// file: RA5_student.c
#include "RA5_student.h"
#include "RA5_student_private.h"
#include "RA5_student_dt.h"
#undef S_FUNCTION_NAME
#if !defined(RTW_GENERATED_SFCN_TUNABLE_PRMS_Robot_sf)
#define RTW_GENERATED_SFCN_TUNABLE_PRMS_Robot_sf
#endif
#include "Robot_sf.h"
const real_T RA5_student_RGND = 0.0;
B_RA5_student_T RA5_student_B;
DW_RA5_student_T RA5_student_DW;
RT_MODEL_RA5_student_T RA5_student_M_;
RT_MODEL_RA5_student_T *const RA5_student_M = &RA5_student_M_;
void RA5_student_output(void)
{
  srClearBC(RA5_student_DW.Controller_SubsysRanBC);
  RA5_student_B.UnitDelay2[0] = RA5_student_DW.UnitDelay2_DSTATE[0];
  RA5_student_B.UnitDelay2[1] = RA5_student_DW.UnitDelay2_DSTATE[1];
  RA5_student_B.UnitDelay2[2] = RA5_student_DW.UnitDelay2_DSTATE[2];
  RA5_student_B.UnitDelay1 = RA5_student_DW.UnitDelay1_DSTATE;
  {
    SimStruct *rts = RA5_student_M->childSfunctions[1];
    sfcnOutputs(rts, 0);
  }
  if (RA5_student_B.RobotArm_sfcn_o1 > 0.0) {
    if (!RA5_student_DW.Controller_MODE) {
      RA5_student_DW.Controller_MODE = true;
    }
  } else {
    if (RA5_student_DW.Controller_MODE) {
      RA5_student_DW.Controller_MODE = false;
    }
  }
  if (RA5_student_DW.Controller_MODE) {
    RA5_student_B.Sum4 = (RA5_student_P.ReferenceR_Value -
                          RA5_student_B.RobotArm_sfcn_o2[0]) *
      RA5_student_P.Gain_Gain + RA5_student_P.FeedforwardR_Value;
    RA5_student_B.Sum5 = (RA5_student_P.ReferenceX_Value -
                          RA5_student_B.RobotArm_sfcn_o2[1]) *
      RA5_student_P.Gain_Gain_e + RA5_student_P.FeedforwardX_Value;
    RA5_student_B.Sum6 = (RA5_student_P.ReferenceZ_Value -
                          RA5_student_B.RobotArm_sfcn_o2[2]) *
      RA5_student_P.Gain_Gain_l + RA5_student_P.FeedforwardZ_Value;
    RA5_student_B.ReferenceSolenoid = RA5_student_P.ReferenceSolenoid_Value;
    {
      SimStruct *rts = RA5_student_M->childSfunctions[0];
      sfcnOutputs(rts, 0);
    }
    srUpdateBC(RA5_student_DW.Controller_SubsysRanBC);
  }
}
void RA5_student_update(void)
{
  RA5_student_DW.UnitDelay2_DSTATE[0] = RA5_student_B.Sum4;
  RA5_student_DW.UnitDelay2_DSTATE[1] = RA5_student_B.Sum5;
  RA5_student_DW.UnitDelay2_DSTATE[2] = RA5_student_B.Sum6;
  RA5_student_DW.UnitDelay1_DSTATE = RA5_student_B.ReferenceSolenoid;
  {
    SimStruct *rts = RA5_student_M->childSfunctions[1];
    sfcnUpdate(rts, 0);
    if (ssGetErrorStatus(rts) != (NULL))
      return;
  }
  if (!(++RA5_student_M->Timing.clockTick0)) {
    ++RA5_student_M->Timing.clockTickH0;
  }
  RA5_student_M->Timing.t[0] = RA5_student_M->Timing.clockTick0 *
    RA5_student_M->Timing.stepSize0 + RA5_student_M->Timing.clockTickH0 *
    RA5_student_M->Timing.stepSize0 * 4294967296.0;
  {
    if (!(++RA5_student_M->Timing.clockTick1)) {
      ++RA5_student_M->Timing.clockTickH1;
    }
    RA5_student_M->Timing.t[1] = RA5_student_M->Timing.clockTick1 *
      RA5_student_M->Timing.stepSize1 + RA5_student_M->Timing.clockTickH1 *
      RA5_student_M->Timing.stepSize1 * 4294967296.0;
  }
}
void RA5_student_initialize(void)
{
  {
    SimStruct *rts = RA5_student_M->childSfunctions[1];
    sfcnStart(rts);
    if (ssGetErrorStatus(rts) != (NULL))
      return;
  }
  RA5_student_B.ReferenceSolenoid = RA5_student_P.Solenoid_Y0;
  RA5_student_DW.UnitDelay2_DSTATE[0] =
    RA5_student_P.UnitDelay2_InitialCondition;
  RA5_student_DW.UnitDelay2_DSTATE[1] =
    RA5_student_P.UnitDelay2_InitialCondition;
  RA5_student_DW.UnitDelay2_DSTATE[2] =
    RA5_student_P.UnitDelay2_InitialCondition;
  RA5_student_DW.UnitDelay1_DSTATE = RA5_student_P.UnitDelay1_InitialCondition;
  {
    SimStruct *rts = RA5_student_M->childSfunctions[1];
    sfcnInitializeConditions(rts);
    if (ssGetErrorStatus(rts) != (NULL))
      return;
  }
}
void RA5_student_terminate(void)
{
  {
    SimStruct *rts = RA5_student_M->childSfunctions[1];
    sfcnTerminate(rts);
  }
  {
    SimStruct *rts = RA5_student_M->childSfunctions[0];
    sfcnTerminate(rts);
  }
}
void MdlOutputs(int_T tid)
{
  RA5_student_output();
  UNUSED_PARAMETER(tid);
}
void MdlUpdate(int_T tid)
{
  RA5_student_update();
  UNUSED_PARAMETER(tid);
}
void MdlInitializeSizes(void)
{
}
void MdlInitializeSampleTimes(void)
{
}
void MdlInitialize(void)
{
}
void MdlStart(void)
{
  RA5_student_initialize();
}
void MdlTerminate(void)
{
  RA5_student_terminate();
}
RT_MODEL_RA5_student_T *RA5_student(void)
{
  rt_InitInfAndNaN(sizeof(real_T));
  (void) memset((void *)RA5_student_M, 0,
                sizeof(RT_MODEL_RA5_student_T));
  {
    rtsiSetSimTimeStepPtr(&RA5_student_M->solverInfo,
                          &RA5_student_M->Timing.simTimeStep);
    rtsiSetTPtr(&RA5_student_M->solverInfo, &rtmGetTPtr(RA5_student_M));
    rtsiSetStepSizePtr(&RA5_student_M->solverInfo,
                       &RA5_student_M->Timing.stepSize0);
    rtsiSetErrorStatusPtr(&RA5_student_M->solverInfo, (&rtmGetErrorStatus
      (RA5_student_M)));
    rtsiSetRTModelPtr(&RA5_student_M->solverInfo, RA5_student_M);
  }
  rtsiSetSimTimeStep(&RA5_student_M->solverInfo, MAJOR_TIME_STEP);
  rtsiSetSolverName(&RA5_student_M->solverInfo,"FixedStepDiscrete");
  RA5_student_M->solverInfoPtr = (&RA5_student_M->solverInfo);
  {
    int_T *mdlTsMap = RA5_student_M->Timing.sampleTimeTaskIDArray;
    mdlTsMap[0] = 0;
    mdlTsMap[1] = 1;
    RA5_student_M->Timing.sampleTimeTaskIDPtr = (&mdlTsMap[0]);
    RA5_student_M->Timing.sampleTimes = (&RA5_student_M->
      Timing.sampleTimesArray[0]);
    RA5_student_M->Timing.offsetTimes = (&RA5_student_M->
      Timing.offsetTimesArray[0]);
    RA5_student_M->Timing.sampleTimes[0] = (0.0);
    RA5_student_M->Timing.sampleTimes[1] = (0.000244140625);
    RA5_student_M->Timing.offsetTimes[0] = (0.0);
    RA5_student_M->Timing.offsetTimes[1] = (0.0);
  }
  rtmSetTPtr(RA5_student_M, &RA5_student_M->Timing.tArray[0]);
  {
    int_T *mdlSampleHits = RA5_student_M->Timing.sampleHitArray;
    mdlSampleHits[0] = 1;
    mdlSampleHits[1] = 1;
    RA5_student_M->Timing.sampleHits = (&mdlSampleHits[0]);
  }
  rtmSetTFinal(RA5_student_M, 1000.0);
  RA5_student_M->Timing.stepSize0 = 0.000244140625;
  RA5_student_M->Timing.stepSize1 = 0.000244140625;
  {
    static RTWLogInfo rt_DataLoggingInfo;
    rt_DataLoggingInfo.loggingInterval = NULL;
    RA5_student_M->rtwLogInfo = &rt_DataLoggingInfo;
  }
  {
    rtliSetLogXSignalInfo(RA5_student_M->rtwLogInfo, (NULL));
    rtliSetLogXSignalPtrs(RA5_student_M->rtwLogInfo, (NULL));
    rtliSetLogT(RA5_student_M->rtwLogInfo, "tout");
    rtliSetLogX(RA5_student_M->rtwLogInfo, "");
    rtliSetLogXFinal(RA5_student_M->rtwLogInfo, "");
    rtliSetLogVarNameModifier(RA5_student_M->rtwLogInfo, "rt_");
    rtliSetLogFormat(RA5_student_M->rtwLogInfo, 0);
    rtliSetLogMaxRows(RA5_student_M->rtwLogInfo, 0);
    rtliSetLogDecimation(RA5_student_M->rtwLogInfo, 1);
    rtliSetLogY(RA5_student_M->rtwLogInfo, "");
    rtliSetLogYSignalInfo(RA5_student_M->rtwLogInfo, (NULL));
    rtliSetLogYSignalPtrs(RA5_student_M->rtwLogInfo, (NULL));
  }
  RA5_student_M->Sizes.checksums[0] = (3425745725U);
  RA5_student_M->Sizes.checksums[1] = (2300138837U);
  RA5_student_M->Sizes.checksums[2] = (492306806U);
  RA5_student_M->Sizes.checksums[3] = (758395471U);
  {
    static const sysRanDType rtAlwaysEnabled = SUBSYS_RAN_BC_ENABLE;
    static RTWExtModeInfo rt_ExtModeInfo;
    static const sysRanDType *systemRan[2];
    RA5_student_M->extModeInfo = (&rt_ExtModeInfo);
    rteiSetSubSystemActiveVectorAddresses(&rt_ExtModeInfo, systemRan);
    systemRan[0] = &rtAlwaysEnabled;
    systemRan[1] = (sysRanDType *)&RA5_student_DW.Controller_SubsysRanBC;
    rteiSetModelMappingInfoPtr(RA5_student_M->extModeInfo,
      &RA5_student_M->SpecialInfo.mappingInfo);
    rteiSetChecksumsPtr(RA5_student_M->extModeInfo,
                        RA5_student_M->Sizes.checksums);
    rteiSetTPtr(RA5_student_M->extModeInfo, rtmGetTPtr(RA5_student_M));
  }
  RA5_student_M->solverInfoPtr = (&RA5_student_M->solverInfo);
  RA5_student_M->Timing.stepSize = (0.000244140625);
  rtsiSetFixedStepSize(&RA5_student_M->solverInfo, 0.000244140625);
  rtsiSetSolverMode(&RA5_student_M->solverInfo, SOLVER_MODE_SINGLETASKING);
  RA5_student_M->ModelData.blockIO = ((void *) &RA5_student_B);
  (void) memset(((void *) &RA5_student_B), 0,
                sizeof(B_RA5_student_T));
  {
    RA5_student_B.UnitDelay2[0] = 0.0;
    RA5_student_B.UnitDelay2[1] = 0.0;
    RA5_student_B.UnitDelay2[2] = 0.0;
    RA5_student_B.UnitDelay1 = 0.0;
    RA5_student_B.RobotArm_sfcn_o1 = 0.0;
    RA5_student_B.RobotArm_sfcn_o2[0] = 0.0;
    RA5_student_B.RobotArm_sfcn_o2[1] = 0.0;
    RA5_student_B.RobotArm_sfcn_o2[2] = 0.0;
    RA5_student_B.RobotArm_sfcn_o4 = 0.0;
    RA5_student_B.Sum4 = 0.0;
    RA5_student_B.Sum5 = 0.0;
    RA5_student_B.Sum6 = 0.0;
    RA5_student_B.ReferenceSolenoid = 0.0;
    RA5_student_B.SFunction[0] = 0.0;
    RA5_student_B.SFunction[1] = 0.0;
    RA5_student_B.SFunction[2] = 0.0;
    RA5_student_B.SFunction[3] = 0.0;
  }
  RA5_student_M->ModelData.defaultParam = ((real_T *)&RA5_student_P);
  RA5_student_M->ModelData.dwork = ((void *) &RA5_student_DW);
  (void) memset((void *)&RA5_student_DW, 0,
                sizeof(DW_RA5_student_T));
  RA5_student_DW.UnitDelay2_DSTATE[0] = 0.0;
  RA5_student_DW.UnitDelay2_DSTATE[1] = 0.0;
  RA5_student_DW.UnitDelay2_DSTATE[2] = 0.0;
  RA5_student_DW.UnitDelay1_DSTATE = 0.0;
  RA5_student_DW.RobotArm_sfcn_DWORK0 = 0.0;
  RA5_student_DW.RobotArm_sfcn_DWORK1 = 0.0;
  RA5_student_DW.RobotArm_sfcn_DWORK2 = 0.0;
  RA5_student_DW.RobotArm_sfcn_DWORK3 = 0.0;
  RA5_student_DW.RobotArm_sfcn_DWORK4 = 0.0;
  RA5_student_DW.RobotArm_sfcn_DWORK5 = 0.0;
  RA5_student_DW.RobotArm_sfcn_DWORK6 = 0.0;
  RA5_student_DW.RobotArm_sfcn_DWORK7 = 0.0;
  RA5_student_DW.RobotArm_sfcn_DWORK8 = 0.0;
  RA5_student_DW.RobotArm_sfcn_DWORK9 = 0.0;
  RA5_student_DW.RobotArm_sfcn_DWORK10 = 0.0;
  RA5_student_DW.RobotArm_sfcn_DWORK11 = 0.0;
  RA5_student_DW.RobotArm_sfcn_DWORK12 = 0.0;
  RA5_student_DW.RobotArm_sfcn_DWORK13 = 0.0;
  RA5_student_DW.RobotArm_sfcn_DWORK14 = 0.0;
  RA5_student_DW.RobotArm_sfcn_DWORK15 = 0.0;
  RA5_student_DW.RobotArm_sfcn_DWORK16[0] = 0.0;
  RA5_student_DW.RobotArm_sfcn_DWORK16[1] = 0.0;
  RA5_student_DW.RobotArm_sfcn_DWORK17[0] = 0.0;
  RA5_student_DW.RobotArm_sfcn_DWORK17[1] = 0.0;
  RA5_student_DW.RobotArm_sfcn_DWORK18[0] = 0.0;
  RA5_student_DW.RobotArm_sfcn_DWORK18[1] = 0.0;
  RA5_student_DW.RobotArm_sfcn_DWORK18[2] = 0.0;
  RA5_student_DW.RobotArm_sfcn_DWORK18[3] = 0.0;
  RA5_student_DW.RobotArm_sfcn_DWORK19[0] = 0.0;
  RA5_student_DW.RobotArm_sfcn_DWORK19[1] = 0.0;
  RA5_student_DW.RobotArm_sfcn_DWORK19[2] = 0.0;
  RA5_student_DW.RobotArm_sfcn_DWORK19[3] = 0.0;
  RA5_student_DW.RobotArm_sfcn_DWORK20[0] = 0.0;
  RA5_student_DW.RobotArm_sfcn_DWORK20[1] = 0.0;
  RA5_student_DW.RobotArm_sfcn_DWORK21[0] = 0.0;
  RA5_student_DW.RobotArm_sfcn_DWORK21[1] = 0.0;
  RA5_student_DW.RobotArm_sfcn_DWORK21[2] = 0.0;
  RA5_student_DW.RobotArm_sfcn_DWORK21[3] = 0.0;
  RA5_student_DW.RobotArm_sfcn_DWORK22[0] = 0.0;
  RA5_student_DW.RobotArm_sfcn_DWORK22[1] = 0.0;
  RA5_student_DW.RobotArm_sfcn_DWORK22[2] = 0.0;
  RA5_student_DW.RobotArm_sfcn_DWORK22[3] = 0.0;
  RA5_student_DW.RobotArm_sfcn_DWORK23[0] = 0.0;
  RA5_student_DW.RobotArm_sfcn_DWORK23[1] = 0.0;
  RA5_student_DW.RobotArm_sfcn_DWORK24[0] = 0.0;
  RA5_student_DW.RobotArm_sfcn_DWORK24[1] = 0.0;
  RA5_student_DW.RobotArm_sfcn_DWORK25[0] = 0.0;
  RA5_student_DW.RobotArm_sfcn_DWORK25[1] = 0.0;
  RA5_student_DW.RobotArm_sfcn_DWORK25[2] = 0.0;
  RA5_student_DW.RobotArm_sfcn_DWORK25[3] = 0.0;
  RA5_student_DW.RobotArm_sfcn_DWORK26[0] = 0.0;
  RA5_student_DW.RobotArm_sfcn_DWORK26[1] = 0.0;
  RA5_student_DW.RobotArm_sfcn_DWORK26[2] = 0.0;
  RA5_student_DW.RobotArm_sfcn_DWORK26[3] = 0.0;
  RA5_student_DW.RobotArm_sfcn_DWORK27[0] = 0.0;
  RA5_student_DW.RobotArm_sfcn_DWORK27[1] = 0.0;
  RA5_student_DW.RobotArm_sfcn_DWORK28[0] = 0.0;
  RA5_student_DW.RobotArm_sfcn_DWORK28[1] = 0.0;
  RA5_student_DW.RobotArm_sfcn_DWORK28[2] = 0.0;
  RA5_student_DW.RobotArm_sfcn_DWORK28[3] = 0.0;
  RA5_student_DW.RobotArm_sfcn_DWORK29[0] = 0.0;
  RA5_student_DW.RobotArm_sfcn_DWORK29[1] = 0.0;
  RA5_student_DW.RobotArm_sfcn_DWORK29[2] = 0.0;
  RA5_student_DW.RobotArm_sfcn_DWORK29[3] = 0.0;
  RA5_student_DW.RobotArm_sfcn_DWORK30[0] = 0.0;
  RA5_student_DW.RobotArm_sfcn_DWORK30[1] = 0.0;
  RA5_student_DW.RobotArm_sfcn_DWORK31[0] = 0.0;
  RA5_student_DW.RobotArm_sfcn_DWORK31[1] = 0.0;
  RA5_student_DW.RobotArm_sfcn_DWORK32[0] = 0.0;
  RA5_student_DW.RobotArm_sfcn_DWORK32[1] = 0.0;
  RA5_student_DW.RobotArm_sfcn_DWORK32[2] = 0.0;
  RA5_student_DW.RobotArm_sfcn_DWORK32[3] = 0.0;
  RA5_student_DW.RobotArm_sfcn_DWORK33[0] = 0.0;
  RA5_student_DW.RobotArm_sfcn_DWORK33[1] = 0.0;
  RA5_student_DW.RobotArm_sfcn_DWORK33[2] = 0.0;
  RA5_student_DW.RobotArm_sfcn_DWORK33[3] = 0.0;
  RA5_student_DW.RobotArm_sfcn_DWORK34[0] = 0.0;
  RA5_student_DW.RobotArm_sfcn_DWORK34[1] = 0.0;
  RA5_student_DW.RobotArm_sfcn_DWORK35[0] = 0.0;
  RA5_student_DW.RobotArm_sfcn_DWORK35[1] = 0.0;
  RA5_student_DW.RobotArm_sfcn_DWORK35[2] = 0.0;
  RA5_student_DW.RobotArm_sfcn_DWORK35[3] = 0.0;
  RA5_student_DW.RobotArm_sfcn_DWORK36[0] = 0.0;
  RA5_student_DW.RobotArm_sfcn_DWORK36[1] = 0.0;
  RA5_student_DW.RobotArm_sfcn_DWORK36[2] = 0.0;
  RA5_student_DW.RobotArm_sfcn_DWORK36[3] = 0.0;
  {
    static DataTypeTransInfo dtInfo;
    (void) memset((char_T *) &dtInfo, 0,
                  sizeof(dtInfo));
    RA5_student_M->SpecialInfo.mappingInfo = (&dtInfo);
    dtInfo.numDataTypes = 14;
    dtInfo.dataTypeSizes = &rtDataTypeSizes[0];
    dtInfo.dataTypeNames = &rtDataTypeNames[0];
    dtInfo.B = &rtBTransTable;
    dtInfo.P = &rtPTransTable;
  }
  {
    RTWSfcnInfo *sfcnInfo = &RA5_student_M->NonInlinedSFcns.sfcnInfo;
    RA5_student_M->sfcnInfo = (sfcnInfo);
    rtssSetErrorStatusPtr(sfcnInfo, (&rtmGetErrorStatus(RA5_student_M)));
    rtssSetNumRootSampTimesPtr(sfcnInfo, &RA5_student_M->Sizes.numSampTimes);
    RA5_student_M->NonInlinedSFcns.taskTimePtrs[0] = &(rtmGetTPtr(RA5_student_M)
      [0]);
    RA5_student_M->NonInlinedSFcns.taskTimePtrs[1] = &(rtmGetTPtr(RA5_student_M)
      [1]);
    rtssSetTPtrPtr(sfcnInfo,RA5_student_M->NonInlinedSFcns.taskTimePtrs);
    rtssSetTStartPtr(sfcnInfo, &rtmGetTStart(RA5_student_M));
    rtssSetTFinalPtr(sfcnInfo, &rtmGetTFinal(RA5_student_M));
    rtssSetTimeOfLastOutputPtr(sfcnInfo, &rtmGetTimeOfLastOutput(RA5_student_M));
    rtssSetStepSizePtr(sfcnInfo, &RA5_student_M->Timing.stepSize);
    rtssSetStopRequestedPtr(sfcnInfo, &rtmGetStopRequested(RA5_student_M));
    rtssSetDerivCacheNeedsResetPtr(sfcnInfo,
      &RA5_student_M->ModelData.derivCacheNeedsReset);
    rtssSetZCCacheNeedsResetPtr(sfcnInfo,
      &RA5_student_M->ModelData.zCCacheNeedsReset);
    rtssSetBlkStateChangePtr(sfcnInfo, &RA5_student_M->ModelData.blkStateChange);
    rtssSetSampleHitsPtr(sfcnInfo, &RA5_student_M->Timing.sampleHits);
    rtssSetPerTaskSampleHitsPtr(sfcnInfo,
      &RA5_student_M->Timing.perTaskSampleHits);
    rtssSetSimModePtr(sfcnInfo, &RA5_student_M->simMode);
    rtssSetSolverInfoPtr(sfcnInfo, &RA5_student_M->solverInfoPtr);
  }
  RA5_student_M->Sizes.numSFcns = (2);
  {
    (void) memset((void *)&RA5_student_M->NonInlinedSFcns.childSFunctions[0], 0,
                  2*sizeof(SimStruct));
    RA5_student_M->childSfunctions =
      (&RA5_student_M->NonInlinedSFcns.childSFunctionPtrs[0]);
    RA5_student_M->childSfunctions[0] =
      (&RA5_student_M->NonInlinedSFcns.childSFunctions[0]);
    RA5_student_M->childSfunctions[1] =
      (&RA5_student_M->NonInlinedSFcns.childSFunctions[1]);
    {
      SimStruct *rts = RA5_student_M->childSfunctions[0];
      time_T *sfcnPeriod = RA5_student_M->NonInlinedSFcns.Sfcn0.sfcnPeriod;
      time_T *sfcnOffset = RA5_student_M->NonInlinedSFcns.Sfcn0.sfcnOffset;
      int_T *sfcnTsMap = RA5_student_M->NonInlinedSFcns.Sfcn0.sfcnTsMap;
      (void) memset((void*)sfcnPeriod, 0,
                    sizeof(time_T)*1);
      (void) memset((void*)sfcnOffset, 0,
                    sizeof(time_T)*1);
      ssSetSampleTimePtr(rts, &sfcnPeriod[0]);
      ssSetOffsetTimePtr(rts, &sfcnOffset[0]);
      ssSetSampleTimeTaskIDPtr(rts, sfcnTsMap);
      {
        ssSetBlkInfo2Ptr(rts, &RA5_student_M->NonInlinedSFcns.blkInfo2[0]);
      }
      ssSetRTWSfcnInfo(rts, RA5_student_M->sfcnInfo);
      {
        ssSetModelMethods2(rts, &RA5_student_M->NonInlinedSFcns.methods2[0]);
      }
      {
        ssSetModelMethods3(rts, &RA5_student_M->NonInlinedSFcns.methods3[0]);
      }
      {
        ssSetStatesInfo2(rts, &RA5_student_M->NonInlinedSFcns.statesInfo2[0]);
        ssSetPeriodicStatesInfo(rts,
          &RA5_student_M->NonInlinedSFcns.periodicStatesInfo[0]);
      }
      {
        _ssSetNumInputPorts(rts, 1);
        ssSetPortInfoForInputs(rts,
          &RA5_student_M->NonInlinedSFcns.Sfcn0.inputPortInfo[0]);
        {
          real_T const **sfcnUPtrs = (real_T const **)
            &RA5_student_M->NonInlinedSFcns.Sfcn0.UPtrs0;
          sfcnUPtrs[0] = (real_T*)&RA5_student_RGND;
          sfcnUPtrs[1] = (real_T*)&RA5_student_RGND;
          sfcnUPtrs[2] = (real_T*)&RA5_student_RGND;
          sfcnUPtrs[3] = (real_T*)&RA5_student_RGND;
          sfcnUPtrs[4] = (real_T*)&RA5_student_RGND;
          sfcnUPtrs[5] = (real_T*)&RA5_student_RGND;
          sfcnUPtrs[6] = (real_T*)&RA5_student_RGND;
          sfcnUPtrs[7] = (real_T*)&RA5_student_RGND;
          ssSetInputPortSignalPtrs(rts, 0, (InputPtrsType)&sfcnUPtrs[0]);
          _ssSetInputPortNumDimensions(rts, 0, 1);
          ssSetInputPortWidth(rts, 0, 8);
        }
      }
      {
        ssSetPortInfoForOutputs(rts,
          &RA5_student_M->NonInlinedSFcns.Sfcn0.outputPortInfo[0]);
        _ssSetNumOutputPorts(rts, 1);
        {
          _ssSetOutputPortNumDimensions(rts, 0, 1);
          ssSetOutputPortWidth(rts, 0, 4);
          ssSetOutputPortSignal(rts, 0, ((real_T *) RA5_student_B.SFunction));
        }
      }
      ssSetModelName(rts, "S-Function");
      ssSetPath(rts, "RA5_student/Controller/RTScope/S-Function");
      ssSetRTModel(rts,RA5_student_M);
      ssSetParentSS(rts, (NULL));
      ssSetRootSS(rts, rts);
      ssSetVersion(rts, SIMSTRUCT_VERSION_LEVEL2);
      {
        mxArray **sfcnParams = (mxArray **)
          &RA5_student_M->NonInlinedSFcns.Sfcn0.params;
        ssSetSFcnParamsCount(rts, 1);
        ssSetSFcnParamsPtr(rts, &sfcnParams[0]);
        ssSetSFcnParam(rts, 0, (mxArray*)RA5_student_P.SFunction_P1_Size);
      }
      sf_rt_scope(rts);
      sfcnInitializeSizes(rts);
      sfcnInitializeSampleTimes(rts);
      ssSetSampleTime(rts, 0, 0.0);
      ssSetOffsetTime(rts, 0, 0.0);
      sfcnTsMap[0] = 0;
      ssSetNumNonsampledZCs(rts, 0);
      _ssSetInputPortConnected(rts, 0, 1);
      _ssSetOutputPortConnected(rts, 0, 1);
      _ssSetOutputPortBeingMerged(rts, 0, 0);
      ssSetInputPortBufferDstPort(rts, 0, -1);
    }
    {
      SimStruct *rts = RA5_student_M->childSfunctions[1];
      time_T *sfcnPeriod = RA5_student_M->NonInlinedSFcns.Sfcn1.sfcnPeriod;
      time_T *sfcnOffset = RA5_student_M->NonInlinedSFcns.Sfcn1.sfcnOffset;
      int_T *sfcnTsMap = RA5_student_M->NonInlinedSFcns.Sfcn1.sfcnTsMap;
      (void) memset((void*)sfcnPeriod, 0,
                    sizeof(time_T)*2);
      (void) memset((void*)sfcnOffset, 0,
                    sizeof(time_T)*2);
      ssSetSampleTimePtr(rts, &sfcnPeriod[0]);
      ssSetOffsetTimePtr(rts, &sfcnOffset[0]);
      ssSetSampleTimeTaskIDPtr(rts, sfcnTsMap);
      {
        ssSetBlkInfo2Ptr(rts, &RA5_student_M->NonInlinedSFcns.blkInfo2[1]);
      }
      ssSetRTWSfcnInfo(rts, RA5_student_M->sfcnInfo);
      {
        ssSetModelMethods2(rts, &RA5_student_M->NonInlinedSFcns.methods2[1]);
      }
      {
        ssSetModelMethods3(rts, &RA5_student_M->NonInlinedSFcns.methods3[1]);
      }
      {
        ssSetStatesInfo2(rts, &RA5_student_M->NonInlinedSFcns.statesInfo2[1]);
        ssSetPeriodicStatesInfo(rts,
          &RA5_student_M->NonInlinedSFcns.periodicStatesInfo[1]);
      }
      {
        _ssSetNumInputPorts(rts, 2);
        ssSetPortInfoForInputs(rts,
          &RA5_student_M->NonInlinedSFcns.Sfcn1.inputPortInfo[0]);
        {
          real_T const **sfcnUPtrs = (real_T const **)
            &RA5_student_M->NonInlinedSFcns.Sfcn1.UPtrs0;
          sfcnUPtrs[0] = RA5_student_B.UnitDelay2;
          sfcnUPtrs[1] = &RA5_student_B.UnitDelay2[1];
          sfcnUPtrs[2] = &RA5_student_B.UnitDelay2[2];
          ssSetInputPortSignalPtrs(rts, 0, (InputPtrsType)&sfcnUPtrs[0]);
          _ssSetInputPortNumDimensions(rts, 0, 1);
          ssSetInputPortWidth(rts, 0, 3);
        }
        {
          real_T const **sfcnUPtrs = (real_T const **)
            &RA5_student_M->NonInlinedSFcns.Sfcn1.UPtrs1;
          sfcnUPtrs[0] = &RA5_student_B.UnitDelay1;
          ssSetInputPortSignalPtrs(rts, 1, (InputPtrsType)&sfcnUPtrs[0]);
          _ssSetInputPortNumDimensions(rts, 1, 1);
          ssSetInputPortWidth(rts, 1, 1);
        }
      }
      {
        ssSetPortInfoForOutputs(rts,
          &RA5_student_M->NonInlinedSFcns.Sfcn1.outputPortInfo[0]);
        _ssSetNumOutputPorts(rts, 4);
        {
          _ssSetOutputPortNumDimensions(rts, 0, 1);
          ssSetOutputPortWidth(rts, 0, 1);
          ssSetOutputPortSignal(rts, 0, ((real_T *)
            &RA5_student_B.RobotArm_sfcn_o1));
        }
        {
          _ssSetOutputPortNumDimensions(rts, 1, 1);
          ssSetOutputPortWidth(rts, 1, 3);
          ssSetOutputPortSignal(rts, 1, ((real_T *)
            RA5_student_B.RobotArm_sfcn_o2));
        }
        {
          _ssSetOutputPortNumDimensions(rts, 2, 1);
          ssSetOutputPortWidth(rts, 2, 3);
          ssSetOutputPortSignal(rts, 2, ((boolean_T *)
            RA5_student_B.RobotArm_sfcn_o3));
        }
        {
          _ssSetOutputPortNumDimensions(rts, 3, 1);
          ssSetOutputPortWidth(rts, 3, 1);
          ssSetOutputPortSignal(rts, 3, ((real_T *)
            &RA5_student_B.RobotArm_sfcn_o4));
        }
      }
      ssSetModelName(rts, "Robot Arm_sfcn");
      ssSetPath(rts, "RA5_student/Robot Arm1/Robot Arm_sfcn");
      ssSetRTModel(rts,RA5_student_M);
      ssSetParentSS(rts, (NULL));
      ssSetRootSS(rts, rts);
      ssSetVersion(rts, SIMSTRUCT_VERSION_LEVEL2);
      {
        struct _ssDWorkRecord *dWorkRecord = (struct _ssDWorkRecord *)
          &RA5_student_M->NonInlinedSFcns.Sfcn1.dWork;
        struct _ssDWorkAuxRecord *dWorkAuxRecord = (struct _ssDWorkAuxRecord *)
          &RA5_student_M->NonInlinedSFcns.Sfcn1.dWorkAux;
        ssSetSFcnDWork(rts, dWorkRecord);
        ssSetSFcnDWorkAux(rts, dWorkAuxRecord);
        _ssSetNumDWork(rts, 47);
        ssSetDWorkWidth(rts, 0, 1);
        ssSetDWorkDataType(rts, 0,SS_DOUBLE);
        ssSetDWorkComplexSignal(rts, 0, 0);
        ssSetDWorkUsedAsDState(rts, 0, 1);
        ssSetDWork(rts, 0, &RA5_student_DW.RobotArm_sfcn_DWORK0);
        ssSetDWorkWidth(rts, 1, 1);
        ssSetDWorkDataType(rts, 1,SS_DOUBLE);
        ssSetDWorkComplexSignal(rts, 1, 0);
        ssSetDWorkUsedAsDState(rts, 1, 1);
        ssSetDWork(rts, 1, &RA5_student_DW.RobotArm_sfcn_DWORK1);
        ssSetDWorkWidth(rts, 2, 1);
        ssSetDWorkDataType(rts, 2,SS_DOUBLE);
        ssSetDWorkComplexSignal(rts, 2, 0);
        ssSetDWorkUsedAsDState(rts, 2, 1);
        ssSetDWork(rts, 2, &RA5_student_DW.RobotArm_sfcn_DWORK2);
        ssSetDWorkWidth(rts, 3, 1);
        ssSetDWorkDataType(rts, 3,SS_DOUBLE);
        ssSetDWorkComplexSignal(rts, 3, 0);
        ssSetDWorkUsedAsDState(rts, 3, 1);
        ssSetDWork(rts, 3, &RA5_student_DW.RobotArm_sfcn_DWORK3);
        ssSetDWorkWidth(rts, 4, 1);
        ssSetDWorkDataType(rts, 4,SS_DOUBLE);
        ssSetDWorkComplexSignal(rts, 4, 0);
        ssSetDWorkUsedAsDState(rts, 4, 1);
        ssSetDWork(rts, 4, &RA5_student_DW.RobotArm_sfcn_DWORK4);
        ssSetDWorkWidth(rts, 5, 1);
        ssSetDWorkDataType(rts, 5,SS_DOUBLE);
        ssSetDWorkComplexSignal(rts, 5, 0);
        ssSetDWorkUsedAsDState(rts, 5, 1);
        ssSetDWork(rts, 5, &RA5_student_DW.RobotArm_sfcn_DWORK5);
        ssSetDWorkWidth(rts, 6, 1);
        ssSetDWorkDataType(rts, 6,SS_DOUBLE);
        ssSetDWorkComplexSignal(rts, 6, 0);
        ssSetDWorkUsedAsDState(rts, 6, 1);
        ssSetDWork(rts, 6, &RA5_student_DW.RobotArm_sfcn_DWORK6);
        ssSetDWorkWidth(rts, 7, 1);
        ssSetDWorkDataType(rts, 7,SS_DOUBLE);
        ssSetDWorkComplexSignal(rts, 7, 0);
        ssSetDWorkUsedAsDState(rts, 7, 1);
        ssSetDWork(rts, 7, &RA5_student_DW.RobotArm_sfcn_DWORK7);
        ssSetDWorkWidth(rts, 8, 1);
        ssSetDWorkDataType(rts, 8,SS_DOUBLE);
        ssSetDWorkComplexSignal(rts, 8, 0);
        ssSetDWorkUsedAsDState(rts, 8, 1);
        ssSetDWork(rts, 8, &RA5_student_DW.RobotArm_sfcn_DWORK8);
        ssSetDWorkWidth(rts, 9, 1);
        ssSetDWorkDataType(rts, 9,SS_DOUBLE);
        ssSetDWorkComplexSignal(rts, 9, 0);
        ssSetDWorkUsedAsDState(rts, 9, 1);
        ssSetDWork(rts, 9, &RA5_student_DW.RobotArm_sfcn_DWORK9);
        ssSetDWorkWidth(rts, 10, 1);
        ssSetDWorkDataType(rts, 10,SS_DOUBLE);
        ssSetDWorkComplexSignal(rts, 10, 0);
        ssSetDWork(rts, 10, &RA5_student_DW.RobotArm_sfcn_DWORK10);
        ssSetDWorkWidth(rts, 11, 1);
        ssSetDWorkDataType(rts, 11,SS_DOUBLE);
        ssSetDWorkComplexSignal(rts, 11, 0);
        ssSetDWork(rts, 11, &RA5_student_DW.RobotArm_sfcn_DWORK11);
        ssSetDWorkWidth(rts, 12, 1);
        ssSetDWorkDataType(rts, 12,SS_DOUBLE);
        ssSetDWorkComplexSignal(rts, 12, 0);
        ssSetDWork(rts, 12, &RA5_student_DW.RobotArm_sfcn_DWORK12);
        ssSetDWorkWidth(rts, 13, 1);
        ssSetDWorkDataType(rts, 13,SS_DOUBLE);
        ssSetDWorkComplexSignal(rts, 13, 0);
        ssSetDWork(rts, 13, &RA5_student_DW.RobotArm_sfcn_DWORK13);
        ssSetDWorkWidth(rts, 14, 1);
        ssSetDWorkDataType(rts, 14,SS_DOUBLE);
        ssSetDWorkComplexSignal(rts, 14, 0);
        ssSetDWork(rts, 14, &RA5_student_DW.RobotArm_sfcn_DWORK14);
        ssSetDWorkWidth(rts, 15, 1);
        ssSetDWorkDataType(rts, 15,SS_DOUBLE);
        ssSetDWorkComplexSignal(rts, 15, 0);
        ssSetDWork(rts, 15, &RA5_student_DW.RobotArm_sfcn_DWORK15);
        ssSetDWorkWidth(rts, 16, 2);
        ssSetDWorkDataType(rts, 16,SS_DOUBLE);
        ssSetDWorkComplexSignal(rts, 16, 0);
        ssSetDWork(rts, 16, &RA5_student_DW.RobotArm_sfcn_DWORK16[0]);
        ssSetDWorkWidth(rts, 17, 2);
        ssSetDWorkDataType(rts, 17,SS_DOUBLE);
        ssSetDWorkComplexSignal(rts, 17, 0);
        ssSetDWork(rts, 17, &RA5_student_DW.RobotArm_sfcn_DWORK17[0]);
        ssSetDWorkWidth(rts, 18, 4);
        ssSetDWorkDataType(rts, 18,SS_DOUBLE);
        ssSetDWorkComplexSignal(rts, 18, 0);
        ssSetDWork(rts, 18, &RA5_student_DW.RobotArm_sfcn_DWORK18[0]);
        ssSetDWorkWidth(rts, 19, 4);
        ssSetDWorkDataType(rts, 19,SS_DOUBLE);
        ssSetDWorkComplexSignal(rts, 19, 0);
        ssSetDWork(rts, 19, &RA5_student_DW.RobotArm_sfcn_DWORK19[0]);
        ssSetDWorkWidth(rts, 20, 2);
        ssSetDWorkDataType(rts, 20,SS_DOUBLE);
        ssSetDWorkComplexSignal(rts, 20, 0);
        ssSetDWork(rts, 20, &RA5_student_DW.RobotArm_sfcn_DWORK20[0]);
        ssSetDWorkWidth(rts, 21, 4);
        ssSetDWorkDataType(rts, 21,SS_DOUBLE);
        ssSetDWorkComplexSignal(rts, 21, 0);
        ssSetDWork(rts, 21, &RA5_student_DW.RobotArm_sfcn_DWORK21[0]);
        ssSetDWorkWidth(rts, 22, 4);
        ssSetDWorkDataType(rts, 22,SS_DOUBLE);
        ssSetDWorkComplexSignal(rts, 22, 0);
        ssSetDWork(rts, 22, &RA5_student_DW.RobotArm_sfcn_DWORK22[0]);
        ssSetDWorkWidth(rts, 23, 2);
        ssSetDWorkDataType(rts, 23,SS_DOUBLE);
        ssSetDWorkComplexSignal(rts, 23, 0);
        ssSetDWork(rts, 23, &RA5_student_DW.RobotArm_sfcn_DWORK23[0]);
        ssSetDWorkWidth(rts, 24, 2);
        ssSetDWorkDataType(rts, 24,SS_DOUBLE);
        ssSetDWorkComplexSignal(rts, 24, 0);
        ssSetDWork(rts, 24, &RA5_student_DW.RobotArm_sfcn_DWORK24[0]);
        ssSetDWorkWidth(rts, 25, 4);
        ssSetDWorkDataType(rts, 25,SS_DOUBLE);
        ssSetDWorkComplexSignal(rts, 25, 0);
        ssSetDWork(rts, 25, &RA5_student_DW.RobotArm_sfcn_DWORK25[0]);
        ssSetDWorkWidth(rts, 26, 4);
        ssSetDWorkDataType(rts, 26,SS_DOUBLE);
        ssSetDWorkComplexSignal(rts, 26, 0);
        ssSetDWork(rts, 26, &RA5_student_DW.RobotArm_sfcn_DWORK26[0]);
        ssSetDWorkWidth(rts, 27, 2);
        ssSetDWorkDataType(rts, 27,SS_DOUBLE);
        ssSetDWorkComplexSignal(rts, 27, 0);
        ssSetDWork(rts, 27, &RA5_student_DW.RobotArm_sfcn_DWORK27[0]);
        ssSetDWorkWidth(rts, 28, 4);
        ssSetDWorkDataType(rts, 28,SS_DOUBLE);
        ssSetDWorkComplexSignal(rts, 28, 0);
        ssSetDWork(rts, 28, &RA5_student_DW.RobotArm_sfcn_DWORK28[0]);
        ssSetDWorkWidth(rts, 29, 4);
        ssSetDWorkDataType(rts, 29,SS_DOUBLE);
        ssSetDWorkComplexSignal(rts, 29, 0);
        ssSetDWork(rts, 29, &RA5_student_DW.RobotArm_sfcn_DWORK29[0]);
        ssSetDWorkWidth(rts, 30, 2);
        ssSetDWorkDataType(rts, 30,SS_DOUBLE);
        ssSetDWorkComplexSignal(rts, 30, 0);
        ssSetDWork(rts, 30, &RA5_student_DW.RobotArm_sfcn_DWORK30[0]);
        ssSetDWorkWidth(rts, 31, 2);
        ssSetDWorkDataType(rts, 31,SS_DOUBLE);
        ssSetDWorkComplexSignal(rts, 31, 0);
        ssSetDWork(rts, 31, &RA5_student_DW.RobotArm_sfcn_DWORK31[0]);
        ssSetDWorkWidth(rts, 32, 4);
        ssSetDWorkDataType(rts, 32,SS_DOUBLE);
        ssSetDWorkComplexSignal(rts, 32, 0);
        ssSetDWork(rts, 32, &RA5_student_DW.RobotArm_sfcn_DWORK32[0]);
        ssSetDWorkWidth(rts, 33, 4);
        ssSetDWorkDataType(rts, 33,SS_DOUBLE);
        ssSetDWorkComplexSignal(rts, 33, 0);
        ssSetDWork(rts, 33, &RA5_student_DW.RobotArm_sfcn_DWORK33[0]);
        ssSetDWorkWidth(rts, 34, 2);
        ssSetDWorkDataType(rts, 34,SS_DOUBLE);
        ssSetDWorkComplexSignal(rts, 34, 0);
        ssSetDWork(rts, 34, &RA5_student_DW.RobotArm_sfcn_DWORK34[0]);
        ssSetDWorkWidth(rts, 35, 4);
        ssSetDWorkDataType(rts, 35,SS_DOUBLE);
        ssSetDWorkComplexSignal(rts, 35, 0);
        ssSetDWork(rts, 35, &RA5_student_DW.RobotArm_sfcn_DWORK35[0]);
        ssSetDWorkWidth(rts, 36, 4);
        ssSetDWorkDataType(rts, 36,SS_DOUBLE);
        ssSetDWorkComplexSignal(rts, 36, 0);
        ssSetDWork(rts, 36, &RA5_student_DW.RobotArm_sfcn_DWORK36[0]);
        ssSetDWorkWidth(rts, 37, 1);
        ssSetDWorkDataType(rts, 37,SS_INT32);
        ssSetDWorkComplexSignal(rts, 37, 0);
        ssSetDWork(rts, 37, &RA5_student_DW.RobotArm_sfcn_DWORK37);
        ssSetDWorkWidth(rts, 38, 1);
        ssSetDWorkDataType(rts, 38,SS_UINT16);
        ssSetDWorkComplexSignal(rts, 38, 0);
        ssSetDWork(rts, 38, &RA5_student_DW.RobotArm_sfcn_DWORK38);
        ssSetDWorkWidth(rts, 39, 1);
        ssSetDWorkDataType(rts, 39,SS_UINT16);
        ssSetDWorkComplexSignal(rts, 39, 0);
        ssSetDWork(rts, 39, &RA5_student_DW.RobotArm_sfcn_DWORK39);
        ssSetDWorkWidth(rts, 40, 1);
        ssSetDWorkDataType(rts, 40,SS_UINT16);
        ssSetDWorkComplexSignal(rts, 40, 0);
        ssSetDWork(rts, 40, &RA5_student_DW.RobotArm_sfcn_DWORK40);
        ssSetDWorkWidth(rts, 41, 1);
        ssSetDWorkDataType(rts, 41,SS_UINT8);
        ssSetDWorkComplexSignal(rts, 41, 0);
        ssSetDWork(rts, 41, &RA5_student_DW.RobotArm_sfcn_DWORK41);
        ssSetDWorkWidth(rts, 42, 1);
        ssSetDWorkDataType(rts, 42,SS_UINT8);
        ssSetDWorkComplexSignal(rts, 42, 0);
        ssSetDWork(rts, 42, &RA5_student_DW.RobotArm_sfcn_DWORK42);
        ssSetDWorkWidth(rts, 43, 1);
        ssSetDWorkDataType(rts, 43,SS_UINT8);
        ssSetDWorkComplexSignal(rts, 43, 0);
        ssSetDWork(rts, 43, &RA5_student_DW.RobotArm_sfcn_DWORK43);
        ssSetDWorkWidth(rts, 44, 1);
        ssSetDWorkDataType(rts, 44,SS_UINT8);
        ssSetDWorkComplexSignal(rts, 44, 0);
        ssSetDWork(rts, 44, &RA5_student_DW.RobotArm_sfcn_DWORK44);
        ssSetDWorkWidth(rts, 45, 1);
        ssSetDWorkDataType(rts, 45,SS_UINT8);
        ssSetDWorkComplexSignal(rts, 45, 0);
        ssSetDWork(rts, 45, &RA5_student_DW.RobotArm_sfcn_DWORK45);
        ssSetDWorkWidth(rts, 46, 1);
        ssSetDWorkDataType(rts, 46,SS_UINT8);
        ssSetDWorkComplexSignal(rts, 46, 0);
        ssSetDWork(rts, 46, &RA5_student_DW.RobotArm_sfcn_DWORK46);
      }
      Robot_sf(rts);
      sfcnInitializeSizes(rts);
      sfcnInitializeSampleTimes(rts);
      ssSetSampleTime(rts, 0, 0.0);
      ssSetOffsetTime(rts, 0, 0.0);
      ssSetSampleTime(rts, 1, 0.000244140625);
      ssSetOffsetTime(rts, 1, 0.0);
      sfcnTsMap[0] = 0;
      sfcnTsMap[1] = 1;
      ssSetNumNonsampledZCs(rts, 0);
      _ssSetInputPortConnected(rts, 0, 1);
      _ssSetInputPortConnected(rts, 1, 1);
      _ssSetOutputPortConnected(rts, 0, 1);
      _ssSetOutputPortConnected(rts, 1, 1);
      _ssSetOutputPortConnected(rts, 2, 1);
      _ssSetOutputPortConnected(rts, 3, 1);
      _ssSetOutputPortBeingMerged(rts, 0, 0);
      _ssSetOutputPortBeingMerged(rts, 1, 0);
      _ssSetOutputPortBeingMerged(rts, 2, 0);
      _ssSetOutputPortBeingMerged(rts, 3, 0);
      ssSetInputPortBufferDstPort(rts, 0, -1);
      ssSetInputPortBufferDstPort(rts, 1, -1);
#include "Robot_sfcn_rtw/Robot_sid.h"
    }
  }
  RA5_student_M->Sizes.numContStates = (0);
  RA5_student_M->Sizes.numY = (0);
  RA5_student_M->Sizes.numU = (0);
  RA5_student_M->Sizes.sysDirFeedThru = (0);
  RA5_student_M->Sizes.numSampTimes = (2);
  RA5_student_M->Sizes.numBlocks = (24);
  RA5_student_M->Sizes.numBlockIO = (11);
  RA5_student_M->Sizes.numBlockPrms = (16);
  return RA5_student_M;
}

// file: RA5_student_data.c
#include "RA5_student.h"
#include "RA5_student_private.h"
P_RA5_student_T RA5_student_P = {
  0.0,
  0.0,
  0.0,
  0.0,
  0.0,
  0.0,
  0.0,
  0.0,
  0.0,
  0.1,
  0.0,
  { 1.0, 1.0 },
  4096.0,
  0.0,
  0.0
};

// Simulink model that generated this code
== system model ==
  UnitDelay2 : UnitDelay  <- 1: Controller
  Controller : Subsystem  <- 1: RobotArm_sfcn/2, Enable: RobotArm_sfcn
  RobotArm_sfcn : S-Function  FunctionName=Robot_sf  <- 1: UnitDelay2, 2: UnitDelay1
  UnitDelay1 : UnitDelay  <- 1: Controller/2
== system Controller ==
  Inport#1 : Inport
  EnablePort#1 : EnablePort
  Outport#1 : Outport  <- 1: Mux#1
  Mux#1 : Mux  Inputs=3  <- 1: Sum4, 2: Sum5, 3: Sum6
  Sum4 : Sum  Inputs=++  <- 1: FeedforwardR, 2: Gain
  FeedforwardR : Constant  Value=0
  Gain : Gain  Gain=0  <- 1: Sum#1
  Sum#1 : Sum  Inputs=+-  <- 1: ReferenceR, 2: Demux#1
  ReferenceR : Constant  Value=0
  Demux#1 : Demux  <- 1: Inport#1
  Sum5 : Sum  Inputs=++  <- 1: FeedforwardX, 2: Gain#1
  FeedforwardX : Constant  Value=0
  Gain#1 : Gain  Gain=0  <- 1: Sum#2
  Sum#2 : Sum  Inputs=+-  <- 1: ReferenceX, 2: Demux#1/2
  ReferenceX : Constant  Value=0
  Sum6 : Sum  Inputs=++  <- 1: FeedforwardZ, 2: Gain#2
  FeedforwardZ : Constant  Value=0.1
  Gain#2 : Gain  Gain=0  <- 1: Sum#3
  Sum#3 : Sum  Inputs=+-  <- 1: ReferenceZ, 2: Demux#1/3
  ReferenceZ : Constant  Value=0
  Solenoid : Outport  InitialOutput=0  <- 1: ReferenceSolenoid
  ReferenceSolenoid : Constant  Value=0
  SFunction : S-Function  FunctionName=sf_rt_scope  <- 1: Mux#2
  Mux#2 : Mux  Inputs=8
